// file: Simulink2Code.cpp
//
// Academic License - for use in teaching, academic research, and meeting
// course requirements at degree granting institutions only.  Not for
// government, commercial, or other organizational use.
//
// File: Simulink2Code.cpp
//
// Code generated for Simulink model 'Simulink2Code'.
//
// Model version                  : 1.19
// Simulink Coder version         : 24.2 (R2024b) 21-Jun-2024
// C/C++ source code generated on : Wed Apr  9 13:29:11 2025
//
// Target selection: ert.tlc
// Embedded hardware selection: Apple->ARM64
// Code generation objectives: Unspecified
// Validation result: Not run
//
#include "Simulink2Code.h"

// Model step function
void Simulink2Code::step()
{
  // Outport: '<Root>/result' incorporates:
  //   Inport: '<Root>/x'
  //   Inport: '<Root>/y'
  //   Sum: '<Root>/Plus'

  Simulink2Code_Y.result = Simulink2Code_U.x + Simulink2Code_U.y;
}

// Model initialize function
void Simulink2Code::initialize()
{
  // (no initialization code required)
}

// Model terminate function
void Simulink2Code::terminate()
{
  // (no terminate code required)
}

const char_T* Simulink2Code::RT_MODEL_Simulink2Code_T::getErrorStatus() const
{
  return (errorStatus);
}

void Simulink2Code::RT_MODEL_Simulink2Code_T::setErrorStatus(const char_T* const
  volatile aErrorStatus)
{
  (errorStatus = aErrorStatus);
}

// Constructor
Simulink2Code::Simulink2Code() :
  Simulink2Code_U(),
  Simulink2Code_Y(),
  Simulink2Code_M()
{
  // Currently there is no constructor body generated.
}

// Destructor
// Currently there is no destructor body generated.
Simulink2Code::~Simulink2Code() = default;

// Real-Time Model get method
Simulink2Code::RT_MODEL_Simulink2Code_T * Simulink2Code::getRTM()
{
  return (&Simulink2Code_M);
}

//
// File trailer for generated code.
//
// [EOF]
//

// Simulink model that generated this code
simulink model "Simulink2Code"  (R2024b)
settings: Solver=FixedStepAuto  StartTime=0.0  StopTime=10.0  FixedStep=1  RelTol=1e-3

== system Simulink2Code ==
  x : Inport
  y : Inport  Port=2
  Plus : Sum
  result : Outport
  wires:
  x/1 -> Plus/1
  y/1 -> Plus/2
  Plus/1 -> result/1
